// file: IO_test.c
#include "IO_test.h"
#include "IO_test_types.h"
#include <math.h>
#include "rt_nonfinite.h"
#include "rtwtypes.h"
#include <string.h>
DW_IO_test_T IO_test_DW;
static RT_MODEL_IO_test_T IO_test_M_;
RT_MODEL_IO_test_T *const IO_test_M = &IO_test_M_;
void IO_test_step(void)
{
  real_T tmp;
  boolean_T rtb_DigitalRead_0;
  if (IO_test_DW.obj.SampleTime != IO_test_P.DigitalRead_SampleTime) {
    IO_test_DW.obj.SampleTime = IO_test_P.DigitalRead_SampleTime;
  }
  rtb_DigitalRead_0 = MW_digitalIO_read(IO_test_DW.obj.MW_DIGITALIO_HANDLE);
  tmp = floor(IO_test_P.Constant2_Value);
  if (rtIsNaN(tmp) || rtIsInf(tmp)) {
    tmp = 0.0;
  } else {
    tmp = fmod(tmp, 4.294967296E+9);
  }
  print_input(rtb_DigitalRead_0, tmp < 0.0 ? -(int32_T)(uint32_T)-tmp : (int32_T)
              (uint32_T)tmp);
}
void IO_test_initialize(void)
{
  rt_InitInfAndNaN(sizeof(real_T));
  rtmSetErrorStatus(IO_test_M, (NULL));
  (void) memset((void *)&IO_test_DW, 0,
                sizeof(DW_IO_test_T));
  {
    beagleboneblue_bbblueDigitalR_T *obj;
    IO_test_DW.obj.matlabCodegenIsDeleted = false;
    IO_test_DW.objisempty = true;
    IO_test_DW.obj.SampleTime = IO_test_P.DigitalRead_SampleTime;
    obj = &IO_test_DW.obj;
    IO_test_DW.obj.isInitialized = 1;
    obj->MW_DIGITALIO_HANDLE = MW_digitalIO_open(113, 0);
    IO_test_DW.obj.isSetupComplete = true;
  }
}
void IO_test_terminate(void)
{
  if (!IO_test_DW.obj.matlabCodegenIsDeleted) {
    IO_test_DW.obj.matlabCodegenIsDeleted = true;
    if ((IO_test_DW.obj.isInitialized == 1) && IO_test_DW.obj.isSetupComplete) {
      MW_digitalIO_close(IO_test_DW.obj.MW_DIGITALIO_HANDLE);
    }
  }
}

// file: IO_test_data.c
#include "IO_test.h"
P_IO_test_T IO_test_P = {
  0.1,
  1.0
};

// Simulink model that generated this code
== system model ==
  CCaller#1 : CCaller  FunctionName=print_input  <- 1: DataTypeConversion#1, 2: DataTypeConversion#2
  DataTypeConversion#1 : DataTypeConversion  <- 1: DigitalRead
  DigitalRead : bbblueBasicLib/Digital Read
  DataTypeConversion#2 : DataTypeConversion  <- 1: Constant2
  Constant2 : Constant
